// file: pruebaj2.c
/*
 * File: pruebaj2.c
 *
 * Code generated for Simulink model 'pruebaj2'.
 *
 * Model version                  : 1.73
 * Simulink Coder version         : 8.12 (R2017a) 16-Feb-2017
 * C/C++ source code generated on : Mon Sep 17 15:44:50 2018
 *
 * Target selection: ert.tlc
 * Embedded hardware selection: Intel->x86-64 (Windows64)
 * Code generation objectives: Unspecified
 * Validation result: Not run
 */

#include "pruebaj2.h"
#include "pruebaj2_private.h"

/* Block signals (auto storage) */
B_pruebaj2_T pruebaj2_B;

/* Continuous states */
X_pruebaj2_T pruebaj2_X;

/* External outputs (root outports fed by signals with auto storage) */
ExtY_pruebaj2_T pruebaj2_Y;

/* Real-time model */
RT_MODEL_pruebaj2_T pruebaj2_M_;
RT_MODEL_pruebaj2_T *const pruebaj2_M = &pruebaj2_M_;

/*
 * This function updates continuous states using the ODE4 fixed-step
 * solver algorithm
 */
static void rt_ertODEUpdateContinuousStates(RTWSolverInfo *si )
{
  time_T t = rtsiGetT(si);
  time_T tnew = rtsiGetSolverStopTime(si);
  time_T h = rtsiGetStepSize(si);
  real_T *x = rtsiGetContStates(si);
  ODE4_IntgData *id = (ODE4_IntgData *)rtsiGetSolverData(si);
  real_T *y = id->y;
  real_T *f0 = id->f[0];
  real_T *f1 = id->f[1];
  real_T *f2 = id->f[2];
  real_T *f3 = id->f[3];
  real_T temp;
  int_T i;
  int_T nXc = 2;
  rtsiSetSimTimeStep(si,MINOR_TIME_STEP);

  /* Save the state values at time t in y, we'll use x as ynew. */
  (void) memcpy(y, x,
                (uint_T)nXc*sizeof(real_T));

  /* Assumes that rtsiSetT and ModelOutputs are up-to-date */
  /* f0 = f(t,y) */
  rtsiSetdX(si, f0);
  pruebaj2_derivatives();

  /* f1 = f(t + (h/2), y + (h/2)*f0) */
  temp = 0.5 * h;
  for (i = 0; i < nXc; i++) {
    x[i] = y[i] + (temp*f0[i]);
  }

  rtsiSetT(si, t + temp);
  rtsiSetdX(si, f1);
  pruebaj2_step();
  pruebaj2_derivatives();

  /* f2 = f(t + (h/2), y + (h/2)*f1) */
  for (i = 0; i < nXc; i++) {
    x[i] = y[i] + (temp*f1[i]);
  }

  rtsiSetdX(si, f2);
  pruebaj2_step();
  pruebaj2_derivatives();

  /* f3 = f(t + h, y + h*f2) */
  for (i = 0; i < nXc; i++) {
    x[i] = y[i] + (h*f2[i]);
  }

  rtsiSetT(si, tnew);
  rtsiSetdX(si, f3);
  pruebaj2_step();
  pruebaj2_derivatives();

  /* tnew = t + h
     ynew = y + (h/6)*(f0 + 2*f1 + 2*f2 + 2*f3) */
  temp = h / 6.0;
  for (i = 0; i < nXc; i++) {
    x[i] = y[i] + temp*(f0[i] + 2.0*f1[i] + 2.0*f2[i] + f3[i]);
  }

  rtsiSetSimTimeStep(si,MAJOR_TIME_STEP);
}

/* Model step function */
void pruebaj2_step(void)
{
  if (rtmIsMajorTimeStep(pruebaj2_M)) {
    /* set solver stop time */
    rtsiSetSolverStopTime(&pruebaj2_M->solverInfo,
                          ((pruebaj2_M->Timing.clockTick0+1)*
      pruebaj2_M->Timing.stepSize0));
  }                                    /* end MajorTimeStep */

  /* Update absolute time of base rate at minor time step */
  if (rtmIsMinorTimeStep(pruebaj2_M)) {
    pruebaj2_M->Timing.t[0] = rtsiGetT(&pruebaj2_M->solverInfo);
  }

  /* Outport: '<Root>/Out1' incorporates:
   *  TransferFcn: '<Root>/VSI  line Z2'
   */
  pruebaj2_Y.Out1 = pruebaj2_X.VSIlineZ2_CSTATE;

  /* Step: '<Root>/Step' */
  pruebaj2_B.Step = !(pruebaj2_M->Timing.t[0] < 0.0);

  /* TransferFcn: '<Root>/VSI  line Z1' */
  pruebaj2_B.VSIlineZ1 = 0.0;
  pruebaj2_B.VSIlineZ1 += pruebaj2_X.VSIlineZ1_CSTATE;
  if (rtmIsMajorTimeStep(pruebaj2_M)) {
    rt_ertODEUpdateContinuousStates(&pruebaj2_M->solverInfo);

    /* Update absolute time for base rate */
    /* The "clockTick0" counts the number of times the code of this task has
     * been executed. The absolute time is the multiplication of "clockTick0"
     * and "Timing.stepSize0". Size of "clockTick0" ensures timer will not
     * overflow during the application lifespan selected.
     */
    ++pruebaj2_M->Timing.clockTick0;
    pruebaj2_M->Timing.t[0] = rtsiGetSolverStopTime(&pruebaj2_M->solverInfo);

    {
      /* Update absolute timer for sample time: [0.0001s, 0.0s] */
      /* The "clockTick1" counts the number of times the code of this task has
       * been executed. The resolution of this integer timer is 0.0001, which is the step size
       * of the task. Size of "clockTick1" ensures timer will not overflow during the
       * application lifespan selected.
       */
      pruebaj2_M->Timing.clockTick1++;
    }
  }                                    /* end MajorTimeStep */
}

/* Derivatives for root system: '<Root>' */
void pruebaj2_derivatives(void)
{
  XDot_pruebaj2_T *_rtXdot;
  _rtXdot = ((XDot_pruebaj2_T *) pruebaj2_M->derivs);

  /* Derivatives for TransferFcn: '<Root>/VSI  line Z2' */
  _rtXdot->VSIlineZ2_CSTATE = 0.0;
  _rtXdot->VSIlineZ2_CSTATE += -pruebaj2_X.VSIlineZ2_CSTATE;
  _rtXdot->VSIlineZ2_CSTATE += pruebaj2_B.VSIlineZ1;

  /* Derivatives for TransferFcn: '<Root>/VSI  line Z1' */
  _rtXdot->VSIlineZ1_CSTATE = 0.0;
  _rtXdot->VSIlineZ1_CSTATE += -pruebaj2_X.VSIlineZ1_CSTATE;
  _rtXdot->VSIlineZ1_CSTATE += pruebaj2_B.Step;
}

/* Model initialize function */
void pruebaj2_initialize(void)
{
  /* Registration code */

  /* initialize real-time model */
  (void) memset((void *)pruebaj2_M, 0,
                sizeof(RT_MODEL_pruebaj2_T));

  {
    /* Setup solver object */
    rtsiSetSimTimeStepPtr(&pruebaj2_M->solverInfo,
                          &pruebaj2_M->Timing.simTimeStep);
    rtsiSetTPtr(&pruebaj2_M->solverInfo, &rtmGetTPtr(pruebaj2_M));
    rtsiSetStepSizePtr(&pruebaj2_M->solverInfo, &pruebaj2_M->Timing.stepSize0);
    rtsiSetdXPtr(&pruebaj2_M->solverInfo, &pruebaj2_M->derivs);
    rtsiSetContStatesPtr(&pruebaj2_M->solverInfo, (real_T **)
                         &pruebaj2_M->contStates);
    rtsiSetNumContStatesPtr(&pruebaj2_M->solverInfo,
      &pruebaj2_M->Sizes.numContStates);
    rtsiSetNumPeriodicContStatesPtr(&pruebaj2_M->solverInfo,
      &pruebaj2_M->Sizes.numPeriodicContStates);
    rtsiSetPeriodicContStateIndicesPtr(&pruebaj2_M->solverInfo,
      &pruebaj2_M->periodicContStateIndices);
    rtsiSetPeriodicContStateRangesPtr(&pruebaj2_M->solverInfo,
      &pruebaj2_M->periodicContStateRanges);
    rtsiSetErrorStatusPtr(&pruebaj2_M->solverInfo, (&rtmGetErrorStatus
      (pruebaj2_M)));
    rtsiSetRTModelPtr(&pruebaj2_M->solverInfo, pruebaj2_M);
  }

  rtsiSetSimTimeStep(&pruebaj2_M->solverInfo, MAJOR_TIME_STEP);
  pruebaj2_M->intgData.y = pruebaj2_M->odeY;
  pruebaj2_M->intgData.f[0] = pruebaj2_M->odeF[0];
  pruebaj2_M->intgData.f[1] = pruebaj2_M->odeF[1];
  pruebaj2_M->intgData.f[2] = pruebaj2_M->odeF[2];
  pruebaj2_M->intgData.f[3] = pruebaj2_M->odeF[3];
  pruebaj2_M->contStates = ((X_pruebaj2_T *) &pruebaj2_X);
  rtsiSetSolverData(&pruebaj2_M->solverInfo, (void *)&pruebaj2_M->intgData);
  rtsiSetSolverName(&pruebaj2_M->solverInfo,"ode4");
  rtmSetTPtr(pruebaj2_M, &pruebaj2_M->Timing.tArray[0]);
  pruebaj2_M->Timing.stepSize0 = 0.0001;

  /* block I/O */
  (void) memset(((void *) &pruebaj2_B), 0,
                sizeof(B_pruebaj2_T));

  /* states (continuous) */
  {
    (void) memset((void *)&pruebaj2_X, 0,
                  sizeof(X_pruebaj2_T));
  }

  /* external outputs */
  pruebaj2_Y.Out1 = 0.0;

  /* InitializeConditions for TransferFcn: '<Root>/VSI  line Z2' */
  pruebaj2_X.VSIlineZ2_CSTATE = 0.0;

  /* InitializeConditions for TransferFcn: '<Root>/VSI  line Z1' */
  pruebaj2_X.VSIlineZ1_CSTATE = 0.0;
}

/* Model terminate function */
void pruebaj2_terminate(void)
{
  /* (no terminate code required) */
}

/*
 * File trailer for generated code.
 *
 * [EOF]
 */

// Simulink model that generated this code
simulink model "pruebaj2"  (R2017a)
settings: Solver=ode4  StartTime=0.0  StopTime=10  FixedStep=1e-4  RelTol=1e-3
InitFcn:
  | SimulinkInit

== system pruebaj2 ==
  Scope : Scope
  Step : Step  Time=0  SampleTime=0
  VSI  line Z1 : TransferFcn  Denominator=[1 1]
  VSI  line Z2 : TransferFcn  Denominator=[1 1]
  Out1 : Outport
  wires:
  VSI  line Z1/1 -> VSI  line Z2/1
  Step/1 -> VSI  line Z1/1
  VSI  line Z2/1 -> Scope/1, Out1/1
